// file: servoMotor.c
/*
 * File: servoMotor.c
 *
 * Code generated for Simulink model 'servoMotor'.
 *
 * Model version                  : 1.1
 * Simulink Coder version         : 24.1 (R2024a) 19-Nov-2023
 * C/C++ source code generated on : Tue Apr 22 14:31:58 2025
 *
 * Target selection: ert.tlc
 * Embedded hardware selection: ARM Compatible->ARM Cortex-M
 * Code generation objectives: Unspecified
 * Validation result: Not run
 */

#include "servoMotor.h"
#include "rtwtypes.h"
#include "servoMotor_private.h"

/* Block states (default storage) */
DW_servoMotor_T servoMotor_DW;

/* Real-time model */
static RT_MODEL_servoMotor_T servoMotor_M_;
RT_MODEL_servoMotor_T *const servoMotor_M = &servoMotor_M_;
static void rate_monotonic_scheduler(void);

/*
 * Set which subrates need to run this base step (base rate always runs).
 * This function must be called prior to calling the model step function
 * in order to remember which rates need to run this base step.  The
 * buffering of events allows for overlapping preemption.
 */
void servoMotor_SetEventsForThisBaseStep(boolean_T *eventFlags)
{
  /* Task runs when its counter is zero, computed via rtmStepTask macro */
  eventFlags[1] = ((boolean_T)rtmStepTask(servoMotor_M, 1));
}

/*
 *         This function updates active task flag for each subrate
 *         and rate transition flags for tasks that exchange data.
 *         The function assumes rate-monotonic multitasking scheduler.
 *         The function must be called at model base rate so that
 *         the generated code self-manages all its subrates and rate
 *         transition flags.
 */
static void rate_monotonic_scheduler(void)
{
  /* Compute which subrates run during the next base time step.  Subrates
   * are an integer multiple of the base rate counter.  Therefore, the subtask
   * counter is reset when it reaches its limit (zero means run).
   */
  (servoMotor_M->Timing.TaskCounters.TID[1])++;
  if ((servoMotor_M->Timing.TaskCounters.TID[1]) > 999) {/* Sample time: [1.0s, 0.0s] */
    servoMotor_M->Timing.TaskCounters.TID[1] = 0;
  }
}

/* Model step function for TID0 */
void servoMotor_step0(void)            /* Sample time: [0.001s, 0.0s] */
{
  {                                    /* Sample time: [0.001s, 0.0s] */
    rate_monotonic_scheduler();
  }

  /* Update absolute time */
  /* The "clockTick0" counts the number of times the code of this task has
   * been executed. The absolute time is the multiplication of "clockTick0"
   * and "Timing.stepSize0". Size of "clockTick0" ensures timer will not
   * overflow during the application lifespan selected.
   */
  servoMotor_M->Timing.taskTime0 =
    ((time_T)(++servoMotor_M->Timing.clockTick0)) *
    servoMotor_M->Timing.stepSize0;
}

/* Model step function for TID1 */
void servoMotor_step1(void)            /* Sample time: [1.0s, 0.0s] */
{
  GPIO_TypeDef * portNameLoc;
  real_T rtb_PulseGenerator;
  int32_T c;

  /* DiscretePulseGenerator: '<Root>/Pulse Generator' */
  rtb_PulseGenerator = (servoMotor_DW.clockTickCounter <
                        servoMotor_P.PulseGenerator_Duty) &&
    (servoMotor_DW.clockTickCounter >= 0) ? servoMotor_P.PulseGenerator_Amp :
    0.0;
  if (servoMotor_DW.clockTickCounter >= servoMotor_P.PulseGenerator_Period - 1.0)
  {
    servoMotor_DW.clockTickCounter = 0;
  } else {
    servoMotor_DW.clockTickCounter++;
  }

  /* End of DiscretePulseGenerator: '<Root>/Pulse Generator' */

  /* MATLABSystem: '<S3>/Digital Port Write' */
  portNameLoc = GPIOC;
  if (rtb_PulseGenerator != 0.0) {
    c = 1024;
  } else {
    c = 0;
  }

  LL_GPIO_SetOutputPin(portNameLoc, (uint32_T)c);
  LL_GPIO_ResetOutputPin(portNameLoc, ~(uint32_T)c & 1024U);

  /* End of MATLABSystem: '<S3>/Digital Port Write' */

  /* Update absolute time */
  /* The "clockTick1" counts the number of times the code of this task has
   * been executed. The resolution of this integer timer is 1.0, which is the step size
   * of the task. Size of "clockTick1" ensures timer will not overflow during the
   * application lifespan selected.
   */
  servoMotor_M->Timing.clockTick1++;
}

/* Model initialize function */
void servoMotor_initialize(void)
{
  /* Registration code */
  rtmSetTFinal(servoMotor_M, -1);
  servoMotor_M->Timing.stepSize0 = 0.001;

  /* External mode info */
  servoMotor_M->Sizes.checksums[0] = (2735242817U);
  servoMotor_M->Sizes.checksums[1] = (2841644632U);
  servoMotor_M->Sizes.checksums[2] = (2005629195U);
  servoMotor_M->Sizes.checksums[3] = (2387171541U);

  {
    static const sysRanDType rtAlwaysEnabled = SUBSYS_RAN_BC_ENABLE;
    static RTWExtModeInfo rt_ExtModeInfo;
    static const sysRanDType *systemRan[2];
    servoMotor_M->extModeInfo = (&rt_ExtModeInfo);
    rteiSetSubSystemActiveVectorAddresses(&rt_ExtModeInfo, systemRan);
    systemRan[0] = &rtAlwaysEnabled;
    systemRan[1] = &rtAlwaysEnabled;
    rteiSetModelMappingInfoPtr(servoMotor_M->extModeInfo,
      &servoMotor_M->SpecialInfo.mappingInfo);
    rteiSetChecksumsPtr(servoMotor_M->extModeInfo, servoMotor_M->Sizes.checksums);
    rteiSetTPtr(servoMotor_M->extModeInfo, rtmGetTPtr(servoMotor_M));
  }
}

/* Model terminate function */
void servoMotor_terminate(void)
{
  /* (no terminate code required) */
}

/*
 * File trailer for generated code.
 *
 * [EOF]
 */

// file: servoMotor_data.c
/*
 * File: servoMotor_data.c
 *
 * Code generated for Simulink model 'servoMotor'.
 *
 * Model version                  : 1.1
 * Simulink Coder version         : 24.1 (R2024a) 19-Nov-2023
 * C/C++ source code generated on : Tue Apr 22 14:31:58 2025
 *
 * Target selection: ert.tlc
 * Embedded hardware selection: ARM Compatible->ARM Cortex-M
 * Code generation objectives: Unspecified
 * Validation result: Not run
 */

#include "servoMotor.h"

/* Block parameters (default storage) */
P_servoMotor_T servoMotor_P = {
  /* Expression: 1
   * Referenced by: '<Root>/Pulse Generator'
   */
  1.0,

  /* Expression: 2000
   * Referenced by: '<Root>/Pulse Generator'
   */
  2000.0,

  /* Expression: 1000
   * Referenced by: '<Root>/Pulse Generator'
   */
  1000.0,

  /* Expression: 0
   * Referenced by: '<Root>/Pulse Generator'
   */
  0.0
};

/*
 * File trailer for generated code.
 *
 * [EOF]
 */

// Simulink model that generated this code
simulink model "servoMotor"  (R2024a)
settings: Solver=FixedStepDiscrete  StartTime=0.0  StopTime=inf  FixedStep=1e-3  RelTol=1e-3  EnableMultiTasking=on
libraries: stm32f4xxblockslib x1

== system servoMotor ==
  Digital Port Write : stm32f4xxblockslib/Digital Port Write  PortName=GPIOC  PinNumber=[10]  ReadOperation=off  IOAsArray=on  EnableSimPort=off  hoistedMaskSrc=ECSoC/ECSimCodegen/Digital Port Write
  Pulse Generator : DiscretePulseGenerator  Period=2000  PulseWidth=1000
  wires:
  Pulse Generator/1 -> Digital Port Write/1
